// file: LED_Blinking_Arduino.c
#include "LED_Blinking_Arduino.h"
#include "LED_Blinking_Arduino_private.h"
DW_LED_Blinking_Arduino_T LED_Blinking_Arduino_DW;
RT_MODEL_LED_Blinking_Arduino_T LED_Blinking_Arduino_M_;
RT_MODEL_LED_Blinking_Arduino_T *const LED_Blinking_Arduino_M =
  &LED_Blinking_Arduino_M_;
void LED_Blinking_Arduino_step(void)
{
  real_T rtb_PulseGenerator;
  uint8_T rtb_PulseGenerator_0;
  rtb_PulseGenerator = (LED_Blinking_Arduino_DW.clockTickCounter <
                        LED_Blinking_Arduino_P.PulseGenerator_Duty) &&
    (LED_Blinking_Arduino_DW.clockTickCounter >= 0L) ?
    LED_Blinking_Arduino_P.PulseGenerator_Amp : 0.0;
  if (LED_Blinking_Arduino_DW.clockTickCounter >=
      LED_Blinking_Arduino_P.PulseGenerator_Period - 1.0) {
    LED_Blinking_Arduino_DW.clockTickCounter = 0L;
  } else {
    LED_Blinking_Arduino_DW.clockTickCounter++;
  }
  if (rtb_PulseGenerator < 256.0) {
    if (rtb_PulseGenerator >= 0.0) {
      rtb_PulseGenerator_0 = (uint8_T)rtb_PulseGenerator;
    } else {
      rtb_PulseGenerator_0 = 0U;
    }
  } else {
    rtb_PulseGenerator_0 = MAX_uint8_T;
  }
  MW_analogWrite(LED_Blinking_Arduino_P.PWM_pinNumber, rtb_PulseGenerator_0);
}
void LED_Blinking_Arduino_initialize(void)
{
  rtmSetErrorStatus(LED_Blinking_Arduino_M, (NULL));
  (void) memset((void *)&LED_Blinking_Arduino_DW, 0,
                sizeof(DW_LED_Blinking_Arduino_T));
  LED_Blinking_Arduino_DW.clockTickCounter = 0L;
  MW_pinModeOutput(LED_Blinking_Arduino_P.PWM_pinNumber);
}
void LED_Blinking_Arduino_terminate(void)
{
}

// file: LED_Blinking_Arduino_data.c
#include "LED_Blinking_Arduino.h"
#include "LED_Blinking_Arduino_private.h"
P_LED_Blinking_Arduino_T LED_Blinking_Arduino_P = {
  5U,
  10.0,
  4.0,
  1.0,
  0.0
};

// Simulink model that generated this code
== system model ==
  PWM : arduinolib/PWM  pinNumber=5  <- 1: PulseGenerator
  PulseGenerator : DiscretePulseGenerator  Amplitude=10  Period=1  PulseWidth=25
